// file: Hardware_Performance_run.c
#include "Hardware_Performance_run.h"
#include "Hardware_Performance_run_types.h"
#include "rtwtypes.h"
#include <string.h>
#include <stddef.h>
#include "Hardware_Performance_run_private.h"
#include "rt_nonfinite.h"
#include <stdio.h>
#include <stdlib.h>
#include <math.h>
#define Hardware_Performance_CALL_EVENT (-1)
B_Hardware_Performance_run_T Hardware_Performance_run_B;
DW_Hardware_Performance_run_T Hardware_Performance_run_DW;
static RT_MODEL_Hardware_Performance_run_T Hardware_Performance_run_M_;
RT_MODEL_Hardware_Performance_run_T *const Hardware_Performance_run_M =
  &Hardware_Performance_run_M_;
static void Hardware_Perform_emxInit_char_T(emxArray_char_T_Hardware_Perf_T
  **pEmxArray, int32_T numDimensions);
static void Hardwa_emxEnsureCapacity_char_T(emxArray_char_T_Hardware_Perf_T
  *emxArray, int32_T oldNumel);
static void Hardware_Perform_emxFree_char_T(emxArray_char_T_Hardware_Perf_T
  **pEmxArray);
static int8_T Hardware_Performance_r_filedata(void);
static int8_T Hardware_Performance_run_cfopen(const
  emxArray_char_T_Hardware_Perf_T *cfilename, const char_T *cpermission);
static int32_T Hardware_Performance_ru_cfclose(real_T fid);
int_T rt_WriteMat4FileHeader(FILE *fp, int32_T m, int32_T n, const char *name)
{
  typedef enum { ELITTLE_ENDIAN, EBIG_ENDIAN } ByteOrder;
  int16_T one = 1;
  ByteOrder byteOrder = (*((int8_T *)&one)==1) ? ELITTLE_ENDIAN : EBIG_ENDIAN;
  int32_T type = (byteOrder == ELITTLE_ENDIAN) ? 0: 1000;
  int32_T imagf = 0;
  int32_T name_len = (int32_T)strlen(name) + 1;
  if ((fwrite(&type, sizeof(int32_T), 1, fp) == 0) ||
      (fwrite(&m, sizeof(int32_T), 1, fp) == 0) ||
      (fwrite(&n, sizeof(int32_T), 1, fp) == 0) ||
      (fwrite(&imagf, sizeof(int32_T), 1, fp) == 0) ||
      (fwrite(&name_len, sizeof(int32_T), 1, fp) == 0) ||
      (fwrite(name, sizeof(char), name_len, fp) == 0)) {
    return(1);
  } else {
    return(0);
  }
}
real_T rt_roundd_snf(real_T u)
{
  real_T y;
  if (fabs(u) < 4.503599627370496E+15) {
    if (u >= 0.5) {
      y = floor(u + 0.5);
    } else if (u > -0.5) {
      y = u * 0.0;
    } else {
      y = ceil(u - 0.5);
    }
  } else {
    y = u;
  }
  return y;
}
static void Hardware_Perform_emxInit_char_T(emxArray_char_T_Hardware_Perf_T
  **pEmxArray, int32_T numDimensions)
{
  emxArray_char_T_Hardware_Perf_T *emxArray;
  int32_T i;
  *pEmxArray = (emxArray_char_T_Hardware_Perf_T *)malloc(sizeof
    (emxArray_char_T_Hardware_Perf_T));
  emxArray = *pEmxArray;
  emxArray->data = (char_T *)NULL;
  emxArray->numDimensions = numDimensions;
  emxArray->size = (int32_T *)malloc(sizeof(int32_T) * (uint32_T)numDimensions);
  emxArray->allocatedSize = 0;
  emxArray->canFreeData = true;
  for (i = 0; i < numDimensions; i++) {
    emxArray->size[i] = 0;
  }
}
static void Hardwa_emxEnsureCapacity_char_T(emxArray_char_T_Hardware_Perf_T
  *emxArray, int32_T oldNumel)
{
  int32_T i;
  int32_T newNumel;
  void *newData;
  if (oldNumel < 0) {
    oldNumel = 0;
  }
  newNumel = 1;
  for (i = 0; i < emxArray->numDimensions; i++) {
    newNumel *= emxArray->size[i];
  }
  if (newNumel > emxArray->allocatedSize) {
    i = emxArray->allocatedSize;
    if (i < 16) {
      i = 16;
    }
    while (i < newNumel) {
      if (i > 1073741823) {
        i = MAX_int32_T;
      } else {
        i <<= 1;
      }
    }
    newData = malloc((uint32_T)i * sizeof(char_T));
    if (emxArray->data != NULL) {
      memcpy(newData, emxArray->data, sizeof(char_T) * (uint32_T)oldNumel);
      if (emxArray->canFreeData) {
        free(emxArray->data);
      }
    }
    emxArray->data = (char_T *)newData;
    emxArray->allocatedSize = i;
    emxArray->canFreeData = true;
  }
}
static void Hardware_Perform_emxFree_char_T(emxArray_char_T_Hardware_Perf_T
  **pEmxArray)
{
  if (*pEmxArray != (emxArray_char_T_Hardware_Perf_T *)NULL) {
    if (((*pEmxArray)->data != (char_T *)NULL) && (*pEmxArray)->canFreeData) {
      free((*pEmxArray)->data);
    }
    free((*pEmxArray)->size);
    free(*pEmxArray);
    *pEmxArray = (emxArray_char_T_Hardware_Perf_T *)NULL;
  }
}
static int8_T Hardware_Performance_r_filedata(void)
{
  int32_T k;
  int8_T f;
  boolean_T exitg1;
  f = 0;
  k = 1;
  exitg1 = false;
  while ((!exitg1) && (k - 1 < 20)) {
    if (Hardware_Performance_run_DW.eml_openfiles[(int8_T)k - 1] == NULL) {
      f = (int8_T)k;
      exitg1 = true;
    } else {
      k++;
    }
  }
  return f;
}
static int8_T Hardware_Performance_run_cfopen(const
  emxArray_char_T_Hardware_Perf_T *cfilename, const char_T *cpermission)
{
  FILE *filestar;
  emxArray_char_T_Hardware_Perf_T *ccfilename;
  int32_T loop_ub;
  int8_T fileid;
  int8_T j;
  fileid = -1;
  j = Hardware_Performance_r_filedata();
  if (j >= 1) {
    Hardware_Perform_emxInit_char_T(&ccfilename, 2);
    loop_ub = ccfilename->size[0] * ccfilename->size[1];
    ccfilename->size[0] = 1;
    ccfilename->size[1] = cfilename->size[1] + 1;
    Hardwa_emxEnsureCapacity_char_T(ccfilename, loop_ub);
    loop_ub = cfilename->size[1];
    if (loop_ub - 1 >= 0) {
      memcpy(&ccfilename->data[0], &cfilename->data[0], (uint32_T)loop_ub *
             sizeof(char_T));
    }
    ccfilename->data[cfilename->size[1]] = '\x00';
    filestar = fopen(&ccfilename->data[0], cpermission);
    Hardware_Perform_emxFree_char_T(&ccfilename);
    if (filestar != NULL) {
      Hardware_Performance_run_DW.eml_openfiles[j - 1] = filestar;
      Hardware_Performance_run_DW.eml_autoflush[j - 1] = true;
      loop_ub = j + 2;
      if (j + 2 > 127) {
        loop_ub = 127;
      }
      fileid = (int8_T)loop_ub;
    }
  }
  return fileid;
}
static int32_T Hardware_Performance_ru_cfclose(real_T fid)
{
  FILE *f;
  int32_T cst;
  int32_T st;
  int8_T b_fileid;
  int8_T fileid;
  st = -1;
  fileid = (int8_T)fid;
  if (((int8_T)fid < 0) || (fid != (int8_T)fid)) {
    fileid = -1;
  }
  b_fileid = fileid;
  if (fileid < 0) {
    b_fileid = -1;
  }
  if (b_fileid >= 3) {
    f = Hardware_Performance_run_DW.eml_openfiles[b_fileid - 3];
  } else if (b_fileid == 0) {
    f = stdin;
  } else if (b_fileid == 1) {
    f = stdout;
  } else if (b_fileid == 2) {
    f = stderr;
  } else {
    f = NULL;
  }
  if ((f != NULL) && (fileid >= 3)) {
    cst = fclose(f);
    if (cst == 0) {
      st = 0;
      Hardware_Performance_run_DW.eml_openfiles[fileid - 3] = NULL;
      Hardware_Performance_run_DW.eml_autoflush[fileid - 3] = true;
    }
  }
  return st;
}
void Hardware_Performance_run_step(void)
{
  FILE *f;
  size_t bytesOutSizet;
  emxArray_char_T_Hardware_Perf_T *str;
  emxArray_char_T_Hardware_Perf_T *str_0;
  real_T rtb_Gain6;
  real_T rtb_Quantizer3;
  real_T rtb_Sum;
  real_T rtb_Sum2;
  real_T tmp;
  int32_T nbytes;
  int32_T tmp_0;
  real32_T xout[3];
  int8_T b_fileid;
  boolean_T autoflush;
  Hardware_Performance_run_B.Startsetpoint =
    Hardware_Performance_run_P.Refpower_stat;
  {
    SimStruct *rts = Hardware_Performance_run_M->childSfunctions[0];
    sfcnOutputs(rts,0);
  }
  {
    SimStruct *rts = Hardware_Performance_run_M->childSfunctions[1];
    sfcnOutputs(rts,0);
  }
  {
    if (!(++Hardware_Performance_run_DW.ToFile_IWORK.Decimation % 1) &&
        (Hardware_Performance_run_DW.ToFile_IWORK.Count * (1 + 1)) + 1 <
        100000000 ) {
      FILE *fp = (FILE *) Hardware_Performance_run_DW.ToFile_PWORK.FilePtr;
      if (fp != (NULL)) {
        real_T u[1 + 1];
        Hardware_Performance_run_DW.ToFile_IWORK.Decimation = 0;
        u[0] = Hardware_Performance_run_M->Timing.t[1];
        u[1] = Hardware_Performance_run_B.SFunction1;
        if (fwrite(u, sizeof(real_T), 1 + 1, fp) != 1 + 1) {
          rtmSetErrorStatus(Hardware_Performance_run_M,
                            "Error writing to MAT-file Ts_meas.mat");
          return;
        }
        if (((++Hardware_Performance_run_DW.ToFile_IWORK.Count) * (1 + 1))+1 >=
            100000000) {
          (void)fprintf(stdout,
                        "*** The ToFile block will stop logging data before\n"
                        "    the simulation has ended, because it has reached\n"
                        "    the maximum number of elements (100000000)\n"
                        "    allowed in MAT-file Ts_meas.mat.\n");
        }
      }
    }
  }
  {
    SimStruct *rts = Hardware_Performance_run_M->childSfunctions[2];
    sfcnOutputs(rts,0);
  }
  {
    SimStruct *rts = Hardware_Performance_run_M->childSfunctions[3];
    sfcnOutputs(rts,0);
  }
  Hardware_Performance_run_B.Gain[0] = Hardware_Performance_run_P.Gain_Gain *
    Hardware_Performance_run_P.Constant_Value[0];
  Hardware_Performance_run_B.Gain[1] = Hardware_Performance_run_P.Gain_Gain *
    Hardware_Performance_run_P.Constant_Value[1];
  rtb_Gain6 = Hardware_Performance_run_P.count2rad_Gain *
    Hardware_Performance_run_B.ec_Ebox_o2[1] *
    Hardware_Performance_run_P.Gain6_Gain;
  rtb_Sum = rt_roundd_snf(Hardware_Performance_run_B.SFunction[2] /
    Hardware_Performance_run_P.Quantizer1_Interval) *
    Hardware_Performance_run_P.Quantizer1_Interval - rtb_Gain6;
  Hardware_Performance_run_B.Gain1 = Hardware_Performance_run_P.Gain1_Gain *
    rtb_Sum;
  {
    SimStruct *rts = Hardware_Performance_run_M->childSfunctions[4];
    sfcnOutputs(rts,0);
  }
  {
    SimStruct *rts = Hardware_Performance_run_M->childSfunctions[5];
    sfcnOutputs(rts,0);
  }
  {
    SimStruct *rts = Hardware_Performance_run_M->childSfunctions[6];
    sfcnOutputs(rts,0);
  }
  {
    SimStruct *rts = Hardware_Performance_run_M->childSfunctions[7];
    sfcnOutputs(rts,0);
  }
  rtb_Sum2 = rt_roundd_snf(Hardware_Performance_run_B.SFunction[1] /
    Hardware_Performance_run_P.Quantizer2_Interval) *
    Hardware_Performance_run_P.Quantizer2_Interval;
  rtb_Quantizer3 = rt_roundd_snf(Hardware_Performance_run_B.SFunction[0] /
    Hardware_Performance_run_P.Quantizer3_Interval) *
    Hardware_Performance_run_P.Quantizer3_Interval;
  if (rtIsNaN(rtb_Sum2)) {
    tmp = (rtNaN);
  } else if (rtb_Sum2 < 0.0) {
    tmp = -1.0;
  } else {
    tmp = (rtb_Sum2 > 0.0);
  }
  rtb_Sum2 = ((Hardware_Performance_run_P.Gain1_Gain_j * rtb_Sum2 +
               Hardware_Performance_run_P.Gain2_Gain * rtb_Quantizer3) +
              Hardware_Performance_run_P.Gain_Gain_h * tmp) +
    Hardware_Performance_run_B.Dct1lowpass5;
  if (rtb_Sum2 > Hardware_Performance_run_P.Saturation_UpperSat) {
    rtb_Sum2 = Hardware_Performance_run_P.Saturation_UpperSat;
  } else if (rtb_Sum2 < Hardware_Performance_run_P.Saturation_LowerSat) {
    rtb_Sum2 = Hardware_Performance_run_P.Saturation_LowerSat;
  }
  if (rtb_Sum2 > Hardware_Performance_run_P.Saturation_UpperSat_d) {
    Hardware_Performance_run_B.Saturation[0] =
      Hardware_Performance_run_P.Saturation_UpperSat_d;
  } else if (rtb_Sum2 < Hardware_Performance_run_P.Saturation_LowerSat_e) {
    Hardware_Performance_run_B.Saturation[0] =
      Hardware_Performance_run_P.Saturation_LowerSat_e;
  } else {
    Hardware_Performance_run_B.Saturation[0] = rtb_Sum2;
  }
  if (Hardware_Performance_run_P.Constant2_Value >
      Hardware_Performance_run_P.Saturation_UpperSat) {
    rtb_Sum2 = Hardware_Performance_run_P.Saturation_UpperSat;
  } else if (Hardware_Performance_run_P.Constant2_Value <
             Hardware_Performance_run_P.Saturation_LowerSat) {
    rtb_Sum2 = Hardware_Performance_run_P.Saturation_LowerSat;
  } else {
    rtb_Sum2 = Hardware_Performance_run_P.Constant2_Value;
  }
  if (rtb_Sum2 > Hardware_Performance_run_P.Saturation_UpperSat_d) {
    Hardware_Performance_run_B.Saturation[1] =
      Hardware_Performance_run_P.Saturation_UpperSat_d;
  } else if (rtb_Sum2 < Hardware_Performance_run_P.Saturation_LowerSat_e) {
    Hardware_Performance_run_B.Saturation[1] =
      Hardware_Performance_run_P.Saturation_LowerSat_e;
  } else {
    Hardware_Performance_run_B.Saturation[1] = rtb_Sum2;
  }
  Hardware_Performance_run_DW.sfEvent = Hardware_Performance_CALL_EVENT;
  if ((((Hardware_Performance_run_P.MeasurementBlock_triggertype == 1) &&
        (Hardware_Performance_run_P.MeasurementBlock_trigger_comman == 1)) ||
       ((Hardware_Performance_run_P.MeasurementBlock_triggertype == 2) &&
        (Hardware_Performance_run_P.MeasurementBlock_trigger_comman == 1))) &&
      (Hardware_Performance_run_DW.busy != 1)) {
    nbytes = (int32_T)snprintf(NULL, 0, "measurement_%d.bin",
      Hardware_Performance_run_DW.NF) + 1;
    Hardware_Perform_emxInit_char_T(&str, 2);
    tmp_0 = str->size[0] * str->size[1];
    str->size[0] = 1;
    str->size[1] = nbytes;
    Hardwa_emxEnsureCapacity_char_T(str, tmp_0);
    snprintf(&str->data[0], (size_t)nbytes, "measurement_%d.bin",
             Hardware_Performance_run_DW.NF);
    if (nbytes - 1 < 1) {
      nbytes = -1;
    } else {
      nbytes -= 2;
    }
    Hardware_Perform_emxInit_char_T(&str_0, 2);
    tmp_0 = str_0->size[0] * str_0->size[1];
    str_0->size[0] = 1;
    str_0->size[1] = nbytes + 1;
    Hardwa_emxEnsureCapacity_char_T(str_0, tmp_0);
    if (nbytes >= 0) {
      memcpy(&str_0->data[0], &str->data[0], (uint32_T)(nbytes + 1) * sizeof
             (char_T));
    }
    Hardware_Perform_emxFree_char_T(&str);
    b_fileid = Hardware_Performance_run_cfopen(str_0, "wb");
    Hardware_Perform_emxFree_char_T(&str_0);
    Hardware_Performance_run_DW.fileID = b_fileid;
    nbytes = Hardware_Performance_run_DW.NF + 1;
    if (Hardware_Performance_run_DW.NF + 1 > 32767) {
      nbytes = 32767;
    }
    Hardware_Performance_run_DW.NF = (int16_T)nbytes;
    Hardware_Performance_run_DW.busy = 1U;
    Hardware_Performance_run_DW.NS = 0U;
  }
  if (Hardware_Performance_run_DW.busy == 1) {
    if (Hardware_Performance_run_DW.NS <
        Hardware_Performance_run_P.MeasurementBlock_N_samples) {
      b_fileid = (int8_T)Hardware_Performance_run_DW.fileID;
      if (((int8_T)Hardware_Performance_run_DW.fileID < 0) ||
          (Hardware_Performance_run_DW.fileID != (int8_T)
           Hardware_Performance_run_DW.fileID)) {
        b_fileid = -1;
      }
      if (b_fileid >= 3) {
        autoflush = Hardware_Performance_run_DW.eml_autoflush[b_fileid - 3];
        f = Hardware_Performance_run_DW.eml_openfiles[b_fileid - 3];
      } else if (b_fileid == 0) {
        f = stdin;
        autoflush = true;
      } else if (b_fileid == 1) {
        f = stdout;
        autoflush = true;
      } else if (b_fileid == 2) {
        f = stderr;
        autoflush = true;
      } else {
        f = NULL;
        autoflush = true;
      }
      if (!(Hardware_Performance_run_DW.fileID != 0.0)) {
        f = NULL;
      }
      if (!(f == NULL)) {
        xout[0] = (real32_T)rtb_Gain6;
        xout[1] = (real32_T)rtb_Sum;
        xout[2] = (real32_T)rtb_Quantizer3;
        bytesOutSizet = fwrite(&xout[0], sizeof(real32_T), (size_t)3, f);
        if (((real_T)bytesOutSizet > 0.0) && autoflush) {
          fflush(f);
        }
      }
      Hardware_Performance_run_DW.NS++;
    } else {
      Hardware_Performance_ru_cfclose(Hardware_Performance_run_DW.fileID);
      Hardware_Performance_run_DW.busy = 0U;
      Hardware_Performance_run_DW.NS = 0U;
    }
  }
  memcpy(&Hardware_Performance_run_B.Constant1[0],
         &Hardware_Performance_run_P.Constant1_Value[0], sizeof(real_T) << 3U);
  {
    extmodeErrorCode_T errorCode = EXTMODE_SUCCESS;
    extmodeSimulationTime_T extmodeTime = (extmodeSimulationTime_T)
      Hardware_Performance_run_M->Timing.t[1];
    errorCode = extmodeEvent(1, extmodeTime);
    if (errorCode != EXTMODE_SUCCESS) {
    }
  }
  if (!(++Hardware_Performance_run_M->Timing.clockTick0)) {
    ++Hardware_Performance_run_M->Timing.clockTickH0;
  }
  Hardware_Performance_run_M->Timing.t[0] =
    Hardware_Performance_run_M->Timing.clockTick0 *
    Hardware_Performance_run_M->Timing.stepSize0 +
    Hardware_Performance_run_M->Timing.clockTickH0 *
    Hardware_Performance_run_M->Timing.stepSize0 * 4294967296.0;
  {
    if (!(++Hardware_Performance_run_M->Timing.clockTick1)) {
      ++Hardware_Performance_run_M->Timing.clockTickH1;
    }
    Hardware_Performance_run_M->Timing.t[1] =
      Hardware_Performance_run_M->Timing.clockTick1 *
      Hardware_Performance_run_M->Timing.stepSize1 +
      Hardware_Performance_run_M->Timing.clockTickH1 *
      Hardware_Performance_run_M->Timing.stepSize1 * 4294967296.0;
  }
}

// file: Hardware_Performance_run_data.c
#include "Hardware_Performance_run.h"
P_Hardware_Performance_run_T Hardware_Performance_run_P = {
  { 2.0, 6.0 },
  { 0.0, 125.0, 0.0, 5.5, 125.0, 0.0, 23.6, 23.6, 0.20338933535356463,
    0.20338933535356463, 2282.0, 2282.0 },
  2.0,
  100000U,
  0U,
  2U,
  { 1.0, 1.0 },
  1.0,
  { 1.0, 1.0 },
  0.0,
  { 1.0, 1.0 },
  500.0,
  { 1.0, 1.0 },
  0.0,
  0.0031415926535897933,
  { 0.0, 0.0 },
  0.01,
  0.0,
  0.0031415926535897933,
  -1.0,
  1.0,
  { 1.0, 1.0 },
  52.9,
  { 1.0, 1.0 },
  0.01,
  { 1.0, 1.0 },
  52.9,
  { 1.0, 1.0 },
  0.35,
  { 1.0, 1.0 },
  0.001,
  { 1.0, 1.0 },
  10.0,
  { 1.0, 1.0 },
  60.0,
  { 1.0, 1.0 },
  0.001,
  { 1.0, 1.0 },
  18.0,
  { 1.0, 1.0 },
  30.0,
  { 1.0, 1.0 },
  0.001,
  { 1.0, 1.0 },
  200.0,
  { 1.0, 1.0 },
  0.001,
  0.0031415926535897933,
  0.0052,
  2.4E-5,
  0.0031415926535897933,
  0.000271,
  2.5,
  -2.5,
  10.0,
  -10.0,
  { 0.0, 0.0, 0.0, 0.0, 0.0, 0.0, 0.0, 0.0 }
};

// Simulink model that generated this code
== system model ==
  MATLABFunction#1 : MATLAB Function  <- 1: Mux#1, 3: Constant#1, 4: Constant#2
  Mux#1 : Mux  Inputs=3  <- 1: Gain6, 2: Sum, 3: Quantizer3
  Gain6 : Gain  Gain=-1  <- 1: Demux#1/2
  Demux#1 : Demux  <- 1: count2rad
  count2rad : Gain  Gain=(2*pi)/(4*500)  <- 1: ec_Ebox/2
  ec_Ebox : S-Function  FunctionName=ec_Ebox  <- 1: Saturation, 2: Gain, 3: Constant1
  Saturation : Saturate  UpperLimit=10  LowerLimit=-10  <- 1: Saturate#1
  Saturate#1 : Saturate  UpperLimit=2.5  LowerLimit=-2.5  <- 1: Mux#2
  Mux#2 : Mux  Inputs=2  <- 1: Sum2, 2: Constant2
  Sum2 : Sum  Inputs=++  <- 1: Sum#1
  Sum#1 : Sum  Inputs=++  <- 1: Gain#1, 2: Sum#2
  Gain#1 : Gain  Gain=0.0052  <- 1: Signum#1
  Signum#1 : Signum  <- 1: Quantizer2
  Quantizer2 : Quantizer  QuantizationInterval=(2*pi)/(500*4)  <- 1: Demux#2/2
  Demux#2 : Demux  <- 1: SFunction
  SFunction : S-Function  FunctionName=ref3b  <- 1: Startsetpoint
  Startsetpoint : Constant  Value=stat
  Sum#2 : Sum  Inputs=++  <- 1: Gain1, 2: Gain2
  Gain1 : Gain  Gain=0.000024  <- 1: Quantizer2
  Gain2 : Gain  Gain=0.000271  <- 1: Quantizer3
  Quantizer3 : Quantizer  QuantizationInterval=(2*pi)/(500*4)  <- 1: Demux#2
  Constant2 : Constant  Value=0
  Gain : Gain  Gain=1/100  <- 1: Constant
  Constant : Constant  Value=[0,0]
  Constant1 : Constant  Value=[0,0,0,0,0,0,0,0]
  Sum : Sum  Inputs=+-  <- 1: Quantizer1, 2: Gain6
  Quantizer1 : Quantizer  QuantizationInterval=(2*pi)/(500*4)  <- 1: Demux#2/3
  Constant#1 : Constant  Value=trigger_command
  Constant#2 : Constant  Value=N_samples
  EthercatSupervisor#1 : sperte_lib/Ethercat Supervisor
== matlab function MATLABFunction#1 ==
function status = perform_measurement(u, trigger_manual, trigger_command, triggertype, N_samples)

%% Persistent variables
persistent fileID NF busy NS

% Init parameters
if isempty(NF)
    NF = int16(0);
end
if isempty(NS)
    NS = uint32(0);
end
if isempty(fileID)
    fileID = 0;
end
if isempty(busy)
    busy = uint8(0);
end

%% Check the triggers
if ( (triggertype == 0 && trigger_manual == 1) || (triggertype == 1 && trigger_command == 1) || (triggertype == 2 && (trigger_command == 1 || trigger_manual == 1) ) )
    if busy == 1
        % We are already busy, nothing to do
    else
        % We should start a new one
        fileID = fopen(sprintf('measurement_%d.bin',NF),'w');  
        NF = NF + 1;
        busy = uint8(1);
        NS = uint32(0);
    end
end

% We have started a measurement
if busy == 1
    if NS < N_samples 
        % Here we write the sample, in single precision float
        fwrite(fileID,u,'single');
        NS = NS + uint32(1);
    else
       % We have N samples already, we are done
       fclose(fileID);
       busy = uint8(0);
       NS = uint32(0);
    end
      
end
    % Output state
    status = uint8(busy);
end
